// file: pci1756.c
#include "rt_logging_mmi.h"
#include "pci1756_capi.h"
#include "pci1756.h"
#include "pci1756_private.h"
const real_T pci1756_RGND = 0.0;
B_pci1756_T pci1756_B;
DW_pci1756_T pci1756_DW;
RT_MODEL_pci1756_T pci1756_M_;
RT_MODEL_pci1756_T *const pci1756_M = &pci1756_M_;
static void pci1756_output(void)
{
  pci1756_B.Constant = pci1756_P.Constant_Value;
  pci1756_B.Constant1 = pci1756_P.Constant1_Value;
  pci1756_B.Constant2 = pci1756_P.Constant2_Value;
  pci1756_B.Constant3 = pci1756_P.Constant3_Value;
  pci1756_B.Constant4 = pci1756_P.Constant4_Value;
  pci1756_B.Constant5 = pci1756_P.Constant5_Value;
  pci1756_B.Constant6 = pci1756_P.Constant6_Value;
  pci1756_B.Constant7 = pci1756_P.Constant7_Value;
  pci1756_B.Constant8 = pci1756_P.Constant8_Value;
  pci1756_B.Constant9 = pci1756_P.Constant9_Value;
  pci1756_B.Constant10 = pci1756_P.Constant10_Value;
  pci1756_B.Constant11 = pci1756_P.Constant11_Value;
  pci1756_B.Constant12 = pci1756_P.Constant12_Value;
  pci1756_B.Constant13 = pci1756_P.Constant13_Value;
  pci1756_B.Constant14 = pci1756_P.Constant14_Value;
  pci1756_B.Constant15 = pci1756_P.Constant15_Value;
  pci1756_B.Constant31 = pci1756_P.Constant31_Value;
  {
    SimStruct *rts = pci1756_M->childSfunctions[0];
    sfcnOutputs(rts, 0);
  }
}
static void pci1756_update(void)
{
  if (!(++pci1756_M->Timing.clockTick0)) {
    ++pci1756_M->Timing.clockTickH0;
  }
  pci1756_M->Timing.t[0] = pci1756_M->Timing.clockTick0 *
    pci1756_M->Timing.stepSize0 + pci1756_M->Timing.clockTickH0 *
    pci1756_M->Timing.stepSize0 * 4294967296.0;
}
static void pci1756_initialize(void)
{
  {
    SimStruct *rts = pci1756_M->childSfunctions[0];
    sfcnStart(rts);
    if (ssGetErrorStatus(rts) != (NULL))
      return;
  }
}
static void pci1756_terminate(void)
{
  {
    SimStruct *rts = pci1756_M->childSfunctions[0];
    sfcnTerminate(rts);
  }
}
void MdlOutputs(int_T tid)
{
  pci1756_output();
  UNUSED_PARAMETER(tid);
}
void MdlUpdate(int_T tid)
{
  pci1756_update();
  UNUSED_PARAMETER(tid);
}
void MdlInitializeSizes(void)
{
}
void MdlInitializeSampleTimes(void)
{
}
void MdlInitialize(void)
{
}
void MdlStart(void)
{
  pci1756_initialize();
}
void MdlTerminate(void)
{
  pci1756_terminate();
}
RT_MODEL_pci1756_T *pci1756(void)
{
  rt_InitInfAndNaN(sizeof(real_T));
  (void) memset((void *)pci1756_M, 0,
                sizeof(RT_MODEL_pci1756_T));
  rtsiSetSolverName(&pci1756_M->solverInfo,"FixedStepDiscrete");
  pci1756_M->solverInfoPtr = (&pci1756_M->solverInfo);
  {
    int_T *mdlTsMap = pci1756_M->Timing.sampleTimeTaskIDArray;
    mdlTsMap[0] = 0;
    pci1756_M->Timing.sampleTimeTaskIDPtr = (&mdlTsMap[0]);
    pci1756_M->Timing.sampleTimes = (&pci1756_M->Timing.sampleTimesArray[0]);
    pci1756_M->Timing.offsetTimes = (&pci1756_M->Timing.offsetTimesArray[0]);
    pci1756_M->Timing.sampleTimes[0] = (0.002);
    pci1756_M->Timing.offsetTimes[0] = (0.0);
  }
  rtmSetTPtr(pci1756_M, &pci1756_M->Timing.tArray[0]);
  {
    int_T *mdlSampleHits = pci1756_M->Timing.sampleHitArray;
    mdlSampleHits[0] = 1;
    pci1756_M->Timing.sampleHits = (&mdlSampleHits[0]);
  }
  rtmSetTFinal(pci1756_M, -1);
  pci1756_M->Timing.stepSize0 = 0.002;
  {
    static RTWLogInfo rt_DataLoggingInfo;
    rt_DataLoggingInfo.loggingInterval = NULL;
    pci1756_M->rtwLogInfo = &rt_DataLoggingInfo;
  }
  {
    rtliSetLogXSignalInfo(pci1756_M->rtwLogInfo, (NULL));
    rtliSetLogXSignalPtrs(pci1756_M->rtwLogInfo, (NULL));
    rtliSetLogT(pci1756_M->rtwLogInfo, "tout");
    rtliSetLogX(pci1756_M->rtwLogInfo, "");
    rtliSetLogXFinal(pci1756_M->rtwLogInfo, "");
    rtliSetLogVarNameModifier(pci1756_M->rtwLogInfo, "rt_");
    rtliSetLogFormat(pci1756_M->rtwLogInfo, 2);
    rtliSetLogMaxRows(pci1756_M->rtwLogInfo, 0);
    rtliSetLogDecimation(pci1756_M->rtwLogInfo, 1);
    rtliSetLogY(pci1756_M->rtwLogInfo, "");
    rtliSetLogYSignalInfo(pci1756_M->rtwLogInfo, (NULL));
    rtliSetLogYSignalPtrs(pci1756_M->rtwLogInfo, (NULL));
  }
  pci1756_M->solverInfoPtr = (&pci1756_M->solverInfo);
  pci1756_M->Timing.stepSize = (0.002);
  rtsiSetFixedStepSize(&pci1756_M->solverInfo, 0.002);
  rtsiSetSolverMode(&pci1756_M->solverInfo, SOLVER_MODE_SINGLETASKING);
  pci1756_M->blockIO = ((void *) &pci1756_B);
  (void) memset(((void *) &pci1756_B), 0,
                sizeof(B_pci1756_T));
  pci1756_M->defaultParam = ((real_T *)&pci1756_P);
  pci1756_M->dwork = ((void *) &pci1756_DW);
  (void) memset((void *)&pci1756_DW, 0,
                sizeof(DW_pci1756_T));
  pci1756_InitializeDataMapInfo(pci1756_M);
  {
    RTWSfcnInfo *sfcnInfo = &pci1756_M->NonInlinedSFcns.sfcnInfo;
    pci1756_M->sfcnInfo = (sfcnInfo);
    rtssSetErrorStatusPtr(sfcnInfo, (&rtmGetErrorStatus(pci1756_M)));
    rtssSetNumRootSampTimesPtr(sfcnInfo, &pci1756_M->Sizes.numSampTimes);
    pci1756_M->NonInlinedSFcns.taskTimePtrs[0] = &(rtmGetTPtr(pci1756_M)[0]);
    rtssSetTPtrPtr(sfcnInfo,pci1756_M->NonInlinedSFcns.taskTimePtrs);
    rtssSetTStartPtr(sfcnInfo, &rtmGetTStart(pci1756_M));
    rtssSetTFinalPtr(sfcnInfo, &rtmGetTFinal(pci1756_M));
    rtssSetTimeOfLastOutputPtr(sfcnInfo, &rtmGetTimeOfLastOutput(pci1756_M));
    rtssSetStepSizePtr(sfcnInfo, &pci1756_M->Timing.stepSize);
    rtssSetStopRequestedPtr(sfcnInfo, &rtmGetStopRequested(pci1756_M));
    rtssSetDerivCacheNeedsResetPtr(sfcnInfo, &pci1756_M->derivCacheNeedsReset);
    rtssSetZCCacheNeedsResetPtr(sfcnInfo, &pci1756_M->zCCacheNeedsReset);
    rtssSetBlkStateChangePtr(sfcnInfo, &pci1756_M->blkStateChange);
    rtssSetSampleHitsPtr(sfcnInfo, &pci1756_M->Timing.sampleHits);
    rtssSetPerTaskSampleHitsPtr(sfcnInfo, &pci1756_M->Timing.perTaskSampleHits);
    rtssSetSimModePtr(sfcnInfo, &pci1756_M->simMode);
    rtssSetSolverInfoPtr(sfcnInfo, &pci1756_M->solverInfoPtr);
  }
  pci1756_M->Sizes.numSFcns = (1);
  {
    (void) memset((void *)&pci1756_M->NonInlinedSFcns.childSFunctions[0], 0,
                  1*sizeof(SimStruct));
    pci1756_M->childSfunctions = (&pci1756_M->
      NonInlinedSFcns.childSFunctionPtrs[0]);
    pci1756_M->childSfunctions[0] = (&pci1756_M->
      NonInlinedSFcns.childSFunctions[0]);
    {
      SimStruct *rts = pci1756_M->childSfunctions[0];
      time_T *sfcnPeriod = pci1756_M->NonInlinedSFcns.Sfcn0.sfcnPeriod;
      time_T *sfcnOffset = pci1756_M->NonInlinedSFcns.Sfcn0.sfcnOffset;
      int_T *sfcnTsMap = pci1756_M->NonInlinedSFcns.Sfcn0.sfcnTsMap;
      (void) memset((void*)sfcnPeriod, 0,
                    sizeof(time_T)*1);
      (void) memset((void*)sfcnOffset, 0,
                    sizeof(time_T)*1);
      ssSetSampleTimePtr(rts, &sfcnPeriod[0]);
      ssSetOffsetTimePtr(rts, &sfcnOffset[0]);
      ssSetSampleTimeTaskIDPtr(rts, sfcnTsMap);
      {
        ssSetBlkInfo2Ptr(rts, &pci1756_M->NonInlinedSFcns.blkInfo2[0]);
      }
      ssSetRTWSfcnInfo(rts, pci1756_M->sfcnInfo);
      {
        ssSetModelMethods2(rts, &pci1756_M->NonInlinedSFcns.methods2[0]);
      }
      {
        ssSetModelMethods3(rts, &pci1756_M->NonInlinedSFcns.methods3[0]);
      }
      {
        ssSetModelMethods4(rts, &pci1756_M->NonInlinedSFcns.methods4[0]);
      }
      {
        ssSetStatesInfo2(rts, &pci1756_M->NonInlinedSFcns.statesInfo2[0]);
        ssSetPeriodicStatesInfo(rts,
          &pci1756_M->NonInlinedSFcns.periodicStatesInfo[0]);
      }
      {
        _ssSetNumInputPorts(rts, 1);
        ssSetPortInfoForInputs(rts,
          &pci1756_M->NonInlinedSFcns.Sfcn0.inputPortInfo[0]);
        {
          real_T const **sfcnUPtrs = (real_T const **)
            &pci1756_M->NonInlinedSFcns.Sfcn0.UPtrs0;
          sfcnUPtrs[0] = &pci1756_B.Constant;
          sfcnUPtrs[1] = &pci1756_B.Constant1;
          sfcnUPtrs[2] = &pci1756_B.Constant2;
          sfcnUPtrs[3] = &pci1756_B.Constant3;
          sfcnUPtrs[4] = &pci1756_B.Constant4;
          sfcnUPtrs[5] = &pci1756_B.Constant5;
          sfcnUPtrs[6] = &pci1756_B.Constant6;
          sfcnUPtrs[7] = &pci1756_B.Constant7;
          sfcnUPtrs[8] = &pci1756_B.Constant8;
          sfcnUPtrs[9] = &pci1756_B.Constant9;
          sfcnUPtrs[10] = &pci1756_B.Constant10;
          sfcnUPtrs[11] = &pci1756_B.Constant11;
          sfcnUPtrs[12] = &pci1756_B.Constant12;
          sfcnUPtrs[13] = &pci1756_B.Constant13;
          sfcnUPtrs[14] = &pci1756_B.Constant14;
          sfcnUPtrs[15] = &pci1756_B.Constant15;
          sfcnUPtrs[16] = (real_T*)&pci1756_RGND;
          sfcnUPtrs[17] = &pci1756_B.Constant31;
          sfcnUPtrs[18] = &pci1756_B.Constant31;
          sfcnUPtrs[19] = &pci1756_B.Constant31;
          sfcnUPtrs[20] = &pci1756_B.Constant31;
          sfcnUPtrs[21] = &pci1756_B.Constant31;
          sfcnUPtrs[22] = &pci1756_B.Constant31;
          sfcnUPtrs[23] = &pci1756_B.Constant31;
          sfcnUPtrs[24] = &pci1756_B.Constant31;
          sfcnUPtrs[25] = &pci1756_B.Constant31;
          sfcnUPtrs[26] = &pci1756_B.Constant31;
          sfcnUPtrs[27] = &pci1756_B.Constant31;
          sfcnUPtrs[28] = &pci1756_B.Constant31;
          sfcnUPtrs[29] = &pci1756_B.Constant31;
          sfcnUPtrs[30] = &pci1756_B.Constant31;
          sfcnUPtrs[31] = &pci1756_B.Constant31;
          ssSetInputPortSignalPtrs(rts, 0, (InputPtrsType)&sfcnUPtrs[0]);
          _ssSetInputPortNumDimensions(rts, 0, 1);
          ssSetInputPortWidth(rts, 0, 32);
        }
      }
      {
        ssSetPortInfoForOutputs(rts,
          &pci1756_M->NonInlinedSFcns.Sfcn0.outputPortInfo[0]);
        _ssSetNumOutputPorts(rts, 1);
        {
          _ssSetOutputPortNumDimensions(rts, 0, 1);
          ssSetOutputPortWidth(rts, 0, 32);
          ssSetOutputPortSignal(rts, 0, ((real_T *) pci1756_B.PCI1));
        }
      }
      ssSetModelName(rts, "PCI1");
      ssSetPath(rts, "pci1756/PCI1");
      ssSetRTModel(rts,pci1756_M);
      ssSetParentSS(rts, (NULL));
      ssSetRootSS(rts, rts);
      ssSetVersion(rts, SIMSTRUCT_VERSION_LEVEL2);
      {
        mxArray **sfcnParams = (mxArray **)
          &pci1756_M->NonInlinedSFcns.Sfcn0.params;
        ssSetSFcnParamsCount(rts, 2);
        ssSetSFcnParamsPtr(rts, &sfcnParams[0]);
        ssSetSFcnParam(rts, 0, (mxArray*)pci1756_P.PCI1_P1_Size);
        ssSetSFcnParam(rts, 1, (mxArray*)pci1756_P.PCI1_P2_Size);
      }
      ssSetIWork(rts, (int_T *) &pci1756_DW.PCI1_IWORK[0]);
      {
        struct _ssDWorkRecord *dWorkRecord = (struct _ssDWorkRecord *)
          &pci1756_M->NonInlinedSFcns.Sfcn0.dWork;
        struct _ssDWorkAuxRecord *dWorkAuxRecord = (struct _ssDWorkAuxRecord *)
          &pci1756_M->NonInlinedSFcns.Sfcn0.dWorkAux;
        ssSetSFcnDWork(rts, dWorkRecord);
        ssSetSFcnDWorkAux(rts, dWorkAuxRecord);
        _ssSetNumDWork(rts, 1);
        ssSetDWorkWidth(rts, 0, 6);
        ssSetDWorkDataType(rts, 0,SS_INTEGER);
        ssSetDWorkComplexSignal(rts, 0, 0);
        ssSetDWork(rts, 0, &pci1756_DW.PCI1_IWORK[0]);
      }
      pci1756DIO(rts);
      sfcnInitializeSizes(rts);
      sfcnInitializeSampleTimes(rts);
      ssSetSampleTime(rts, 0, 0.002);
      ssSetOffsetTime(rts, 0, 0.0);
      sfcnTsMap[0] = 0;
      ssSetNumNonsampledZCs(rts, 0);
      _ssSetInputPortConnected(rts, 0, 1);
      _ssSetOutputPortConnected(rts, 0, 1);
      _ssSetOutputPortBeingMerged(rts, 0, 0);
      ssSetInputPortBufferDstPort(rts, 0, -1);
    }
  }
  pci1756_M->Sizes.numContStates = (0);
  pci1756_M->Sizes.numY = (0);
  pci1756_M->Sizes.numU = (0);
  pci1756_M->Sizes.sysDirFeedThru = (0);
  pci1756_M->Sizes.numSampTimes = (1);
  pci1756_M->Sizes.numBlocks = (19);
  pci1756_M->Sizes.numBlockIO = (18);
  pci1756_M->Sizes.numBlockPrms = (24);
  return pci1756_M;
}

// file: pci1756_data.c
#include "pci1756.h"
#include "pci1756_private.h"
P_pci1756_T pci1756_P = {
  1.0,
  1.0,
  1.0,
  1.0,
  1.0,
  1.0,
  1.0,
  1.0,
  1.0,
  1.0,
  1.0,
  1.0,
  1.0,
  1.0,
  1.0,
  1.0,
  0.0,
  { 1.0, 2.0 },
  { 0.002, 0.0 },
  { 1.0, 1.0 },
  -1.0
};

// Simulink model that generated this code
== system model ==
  PCI1 : S-Function  FunctionName=pci1756DIO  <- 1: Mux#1
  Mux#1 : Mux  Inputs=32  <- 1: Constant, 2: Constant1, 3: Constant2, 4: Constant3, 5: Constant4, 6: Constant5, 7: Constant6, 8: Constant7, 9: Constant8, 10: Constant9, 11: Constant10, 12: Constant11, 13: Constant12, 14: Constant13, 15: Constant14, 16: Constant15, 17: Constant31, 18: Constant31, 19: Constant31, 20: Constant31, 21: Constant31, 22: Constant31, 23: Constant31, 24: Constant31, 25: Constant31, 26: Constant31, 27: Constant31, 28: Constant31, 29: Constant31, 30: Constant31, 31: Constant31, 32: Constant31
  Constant : Constant
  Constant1 : Constant
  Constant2 : Constant
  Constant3 : Constant
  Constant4 : Constant
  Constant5 : Constant
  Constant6 : Constant
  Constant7 : Constant
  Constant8 : Constant
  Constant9 : Constant
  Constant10 : Constant
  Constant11 : Constant
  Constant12 : Constant
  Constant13 : Constant
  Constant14 : Constant
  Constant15 : Constant
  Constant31 : Constant
